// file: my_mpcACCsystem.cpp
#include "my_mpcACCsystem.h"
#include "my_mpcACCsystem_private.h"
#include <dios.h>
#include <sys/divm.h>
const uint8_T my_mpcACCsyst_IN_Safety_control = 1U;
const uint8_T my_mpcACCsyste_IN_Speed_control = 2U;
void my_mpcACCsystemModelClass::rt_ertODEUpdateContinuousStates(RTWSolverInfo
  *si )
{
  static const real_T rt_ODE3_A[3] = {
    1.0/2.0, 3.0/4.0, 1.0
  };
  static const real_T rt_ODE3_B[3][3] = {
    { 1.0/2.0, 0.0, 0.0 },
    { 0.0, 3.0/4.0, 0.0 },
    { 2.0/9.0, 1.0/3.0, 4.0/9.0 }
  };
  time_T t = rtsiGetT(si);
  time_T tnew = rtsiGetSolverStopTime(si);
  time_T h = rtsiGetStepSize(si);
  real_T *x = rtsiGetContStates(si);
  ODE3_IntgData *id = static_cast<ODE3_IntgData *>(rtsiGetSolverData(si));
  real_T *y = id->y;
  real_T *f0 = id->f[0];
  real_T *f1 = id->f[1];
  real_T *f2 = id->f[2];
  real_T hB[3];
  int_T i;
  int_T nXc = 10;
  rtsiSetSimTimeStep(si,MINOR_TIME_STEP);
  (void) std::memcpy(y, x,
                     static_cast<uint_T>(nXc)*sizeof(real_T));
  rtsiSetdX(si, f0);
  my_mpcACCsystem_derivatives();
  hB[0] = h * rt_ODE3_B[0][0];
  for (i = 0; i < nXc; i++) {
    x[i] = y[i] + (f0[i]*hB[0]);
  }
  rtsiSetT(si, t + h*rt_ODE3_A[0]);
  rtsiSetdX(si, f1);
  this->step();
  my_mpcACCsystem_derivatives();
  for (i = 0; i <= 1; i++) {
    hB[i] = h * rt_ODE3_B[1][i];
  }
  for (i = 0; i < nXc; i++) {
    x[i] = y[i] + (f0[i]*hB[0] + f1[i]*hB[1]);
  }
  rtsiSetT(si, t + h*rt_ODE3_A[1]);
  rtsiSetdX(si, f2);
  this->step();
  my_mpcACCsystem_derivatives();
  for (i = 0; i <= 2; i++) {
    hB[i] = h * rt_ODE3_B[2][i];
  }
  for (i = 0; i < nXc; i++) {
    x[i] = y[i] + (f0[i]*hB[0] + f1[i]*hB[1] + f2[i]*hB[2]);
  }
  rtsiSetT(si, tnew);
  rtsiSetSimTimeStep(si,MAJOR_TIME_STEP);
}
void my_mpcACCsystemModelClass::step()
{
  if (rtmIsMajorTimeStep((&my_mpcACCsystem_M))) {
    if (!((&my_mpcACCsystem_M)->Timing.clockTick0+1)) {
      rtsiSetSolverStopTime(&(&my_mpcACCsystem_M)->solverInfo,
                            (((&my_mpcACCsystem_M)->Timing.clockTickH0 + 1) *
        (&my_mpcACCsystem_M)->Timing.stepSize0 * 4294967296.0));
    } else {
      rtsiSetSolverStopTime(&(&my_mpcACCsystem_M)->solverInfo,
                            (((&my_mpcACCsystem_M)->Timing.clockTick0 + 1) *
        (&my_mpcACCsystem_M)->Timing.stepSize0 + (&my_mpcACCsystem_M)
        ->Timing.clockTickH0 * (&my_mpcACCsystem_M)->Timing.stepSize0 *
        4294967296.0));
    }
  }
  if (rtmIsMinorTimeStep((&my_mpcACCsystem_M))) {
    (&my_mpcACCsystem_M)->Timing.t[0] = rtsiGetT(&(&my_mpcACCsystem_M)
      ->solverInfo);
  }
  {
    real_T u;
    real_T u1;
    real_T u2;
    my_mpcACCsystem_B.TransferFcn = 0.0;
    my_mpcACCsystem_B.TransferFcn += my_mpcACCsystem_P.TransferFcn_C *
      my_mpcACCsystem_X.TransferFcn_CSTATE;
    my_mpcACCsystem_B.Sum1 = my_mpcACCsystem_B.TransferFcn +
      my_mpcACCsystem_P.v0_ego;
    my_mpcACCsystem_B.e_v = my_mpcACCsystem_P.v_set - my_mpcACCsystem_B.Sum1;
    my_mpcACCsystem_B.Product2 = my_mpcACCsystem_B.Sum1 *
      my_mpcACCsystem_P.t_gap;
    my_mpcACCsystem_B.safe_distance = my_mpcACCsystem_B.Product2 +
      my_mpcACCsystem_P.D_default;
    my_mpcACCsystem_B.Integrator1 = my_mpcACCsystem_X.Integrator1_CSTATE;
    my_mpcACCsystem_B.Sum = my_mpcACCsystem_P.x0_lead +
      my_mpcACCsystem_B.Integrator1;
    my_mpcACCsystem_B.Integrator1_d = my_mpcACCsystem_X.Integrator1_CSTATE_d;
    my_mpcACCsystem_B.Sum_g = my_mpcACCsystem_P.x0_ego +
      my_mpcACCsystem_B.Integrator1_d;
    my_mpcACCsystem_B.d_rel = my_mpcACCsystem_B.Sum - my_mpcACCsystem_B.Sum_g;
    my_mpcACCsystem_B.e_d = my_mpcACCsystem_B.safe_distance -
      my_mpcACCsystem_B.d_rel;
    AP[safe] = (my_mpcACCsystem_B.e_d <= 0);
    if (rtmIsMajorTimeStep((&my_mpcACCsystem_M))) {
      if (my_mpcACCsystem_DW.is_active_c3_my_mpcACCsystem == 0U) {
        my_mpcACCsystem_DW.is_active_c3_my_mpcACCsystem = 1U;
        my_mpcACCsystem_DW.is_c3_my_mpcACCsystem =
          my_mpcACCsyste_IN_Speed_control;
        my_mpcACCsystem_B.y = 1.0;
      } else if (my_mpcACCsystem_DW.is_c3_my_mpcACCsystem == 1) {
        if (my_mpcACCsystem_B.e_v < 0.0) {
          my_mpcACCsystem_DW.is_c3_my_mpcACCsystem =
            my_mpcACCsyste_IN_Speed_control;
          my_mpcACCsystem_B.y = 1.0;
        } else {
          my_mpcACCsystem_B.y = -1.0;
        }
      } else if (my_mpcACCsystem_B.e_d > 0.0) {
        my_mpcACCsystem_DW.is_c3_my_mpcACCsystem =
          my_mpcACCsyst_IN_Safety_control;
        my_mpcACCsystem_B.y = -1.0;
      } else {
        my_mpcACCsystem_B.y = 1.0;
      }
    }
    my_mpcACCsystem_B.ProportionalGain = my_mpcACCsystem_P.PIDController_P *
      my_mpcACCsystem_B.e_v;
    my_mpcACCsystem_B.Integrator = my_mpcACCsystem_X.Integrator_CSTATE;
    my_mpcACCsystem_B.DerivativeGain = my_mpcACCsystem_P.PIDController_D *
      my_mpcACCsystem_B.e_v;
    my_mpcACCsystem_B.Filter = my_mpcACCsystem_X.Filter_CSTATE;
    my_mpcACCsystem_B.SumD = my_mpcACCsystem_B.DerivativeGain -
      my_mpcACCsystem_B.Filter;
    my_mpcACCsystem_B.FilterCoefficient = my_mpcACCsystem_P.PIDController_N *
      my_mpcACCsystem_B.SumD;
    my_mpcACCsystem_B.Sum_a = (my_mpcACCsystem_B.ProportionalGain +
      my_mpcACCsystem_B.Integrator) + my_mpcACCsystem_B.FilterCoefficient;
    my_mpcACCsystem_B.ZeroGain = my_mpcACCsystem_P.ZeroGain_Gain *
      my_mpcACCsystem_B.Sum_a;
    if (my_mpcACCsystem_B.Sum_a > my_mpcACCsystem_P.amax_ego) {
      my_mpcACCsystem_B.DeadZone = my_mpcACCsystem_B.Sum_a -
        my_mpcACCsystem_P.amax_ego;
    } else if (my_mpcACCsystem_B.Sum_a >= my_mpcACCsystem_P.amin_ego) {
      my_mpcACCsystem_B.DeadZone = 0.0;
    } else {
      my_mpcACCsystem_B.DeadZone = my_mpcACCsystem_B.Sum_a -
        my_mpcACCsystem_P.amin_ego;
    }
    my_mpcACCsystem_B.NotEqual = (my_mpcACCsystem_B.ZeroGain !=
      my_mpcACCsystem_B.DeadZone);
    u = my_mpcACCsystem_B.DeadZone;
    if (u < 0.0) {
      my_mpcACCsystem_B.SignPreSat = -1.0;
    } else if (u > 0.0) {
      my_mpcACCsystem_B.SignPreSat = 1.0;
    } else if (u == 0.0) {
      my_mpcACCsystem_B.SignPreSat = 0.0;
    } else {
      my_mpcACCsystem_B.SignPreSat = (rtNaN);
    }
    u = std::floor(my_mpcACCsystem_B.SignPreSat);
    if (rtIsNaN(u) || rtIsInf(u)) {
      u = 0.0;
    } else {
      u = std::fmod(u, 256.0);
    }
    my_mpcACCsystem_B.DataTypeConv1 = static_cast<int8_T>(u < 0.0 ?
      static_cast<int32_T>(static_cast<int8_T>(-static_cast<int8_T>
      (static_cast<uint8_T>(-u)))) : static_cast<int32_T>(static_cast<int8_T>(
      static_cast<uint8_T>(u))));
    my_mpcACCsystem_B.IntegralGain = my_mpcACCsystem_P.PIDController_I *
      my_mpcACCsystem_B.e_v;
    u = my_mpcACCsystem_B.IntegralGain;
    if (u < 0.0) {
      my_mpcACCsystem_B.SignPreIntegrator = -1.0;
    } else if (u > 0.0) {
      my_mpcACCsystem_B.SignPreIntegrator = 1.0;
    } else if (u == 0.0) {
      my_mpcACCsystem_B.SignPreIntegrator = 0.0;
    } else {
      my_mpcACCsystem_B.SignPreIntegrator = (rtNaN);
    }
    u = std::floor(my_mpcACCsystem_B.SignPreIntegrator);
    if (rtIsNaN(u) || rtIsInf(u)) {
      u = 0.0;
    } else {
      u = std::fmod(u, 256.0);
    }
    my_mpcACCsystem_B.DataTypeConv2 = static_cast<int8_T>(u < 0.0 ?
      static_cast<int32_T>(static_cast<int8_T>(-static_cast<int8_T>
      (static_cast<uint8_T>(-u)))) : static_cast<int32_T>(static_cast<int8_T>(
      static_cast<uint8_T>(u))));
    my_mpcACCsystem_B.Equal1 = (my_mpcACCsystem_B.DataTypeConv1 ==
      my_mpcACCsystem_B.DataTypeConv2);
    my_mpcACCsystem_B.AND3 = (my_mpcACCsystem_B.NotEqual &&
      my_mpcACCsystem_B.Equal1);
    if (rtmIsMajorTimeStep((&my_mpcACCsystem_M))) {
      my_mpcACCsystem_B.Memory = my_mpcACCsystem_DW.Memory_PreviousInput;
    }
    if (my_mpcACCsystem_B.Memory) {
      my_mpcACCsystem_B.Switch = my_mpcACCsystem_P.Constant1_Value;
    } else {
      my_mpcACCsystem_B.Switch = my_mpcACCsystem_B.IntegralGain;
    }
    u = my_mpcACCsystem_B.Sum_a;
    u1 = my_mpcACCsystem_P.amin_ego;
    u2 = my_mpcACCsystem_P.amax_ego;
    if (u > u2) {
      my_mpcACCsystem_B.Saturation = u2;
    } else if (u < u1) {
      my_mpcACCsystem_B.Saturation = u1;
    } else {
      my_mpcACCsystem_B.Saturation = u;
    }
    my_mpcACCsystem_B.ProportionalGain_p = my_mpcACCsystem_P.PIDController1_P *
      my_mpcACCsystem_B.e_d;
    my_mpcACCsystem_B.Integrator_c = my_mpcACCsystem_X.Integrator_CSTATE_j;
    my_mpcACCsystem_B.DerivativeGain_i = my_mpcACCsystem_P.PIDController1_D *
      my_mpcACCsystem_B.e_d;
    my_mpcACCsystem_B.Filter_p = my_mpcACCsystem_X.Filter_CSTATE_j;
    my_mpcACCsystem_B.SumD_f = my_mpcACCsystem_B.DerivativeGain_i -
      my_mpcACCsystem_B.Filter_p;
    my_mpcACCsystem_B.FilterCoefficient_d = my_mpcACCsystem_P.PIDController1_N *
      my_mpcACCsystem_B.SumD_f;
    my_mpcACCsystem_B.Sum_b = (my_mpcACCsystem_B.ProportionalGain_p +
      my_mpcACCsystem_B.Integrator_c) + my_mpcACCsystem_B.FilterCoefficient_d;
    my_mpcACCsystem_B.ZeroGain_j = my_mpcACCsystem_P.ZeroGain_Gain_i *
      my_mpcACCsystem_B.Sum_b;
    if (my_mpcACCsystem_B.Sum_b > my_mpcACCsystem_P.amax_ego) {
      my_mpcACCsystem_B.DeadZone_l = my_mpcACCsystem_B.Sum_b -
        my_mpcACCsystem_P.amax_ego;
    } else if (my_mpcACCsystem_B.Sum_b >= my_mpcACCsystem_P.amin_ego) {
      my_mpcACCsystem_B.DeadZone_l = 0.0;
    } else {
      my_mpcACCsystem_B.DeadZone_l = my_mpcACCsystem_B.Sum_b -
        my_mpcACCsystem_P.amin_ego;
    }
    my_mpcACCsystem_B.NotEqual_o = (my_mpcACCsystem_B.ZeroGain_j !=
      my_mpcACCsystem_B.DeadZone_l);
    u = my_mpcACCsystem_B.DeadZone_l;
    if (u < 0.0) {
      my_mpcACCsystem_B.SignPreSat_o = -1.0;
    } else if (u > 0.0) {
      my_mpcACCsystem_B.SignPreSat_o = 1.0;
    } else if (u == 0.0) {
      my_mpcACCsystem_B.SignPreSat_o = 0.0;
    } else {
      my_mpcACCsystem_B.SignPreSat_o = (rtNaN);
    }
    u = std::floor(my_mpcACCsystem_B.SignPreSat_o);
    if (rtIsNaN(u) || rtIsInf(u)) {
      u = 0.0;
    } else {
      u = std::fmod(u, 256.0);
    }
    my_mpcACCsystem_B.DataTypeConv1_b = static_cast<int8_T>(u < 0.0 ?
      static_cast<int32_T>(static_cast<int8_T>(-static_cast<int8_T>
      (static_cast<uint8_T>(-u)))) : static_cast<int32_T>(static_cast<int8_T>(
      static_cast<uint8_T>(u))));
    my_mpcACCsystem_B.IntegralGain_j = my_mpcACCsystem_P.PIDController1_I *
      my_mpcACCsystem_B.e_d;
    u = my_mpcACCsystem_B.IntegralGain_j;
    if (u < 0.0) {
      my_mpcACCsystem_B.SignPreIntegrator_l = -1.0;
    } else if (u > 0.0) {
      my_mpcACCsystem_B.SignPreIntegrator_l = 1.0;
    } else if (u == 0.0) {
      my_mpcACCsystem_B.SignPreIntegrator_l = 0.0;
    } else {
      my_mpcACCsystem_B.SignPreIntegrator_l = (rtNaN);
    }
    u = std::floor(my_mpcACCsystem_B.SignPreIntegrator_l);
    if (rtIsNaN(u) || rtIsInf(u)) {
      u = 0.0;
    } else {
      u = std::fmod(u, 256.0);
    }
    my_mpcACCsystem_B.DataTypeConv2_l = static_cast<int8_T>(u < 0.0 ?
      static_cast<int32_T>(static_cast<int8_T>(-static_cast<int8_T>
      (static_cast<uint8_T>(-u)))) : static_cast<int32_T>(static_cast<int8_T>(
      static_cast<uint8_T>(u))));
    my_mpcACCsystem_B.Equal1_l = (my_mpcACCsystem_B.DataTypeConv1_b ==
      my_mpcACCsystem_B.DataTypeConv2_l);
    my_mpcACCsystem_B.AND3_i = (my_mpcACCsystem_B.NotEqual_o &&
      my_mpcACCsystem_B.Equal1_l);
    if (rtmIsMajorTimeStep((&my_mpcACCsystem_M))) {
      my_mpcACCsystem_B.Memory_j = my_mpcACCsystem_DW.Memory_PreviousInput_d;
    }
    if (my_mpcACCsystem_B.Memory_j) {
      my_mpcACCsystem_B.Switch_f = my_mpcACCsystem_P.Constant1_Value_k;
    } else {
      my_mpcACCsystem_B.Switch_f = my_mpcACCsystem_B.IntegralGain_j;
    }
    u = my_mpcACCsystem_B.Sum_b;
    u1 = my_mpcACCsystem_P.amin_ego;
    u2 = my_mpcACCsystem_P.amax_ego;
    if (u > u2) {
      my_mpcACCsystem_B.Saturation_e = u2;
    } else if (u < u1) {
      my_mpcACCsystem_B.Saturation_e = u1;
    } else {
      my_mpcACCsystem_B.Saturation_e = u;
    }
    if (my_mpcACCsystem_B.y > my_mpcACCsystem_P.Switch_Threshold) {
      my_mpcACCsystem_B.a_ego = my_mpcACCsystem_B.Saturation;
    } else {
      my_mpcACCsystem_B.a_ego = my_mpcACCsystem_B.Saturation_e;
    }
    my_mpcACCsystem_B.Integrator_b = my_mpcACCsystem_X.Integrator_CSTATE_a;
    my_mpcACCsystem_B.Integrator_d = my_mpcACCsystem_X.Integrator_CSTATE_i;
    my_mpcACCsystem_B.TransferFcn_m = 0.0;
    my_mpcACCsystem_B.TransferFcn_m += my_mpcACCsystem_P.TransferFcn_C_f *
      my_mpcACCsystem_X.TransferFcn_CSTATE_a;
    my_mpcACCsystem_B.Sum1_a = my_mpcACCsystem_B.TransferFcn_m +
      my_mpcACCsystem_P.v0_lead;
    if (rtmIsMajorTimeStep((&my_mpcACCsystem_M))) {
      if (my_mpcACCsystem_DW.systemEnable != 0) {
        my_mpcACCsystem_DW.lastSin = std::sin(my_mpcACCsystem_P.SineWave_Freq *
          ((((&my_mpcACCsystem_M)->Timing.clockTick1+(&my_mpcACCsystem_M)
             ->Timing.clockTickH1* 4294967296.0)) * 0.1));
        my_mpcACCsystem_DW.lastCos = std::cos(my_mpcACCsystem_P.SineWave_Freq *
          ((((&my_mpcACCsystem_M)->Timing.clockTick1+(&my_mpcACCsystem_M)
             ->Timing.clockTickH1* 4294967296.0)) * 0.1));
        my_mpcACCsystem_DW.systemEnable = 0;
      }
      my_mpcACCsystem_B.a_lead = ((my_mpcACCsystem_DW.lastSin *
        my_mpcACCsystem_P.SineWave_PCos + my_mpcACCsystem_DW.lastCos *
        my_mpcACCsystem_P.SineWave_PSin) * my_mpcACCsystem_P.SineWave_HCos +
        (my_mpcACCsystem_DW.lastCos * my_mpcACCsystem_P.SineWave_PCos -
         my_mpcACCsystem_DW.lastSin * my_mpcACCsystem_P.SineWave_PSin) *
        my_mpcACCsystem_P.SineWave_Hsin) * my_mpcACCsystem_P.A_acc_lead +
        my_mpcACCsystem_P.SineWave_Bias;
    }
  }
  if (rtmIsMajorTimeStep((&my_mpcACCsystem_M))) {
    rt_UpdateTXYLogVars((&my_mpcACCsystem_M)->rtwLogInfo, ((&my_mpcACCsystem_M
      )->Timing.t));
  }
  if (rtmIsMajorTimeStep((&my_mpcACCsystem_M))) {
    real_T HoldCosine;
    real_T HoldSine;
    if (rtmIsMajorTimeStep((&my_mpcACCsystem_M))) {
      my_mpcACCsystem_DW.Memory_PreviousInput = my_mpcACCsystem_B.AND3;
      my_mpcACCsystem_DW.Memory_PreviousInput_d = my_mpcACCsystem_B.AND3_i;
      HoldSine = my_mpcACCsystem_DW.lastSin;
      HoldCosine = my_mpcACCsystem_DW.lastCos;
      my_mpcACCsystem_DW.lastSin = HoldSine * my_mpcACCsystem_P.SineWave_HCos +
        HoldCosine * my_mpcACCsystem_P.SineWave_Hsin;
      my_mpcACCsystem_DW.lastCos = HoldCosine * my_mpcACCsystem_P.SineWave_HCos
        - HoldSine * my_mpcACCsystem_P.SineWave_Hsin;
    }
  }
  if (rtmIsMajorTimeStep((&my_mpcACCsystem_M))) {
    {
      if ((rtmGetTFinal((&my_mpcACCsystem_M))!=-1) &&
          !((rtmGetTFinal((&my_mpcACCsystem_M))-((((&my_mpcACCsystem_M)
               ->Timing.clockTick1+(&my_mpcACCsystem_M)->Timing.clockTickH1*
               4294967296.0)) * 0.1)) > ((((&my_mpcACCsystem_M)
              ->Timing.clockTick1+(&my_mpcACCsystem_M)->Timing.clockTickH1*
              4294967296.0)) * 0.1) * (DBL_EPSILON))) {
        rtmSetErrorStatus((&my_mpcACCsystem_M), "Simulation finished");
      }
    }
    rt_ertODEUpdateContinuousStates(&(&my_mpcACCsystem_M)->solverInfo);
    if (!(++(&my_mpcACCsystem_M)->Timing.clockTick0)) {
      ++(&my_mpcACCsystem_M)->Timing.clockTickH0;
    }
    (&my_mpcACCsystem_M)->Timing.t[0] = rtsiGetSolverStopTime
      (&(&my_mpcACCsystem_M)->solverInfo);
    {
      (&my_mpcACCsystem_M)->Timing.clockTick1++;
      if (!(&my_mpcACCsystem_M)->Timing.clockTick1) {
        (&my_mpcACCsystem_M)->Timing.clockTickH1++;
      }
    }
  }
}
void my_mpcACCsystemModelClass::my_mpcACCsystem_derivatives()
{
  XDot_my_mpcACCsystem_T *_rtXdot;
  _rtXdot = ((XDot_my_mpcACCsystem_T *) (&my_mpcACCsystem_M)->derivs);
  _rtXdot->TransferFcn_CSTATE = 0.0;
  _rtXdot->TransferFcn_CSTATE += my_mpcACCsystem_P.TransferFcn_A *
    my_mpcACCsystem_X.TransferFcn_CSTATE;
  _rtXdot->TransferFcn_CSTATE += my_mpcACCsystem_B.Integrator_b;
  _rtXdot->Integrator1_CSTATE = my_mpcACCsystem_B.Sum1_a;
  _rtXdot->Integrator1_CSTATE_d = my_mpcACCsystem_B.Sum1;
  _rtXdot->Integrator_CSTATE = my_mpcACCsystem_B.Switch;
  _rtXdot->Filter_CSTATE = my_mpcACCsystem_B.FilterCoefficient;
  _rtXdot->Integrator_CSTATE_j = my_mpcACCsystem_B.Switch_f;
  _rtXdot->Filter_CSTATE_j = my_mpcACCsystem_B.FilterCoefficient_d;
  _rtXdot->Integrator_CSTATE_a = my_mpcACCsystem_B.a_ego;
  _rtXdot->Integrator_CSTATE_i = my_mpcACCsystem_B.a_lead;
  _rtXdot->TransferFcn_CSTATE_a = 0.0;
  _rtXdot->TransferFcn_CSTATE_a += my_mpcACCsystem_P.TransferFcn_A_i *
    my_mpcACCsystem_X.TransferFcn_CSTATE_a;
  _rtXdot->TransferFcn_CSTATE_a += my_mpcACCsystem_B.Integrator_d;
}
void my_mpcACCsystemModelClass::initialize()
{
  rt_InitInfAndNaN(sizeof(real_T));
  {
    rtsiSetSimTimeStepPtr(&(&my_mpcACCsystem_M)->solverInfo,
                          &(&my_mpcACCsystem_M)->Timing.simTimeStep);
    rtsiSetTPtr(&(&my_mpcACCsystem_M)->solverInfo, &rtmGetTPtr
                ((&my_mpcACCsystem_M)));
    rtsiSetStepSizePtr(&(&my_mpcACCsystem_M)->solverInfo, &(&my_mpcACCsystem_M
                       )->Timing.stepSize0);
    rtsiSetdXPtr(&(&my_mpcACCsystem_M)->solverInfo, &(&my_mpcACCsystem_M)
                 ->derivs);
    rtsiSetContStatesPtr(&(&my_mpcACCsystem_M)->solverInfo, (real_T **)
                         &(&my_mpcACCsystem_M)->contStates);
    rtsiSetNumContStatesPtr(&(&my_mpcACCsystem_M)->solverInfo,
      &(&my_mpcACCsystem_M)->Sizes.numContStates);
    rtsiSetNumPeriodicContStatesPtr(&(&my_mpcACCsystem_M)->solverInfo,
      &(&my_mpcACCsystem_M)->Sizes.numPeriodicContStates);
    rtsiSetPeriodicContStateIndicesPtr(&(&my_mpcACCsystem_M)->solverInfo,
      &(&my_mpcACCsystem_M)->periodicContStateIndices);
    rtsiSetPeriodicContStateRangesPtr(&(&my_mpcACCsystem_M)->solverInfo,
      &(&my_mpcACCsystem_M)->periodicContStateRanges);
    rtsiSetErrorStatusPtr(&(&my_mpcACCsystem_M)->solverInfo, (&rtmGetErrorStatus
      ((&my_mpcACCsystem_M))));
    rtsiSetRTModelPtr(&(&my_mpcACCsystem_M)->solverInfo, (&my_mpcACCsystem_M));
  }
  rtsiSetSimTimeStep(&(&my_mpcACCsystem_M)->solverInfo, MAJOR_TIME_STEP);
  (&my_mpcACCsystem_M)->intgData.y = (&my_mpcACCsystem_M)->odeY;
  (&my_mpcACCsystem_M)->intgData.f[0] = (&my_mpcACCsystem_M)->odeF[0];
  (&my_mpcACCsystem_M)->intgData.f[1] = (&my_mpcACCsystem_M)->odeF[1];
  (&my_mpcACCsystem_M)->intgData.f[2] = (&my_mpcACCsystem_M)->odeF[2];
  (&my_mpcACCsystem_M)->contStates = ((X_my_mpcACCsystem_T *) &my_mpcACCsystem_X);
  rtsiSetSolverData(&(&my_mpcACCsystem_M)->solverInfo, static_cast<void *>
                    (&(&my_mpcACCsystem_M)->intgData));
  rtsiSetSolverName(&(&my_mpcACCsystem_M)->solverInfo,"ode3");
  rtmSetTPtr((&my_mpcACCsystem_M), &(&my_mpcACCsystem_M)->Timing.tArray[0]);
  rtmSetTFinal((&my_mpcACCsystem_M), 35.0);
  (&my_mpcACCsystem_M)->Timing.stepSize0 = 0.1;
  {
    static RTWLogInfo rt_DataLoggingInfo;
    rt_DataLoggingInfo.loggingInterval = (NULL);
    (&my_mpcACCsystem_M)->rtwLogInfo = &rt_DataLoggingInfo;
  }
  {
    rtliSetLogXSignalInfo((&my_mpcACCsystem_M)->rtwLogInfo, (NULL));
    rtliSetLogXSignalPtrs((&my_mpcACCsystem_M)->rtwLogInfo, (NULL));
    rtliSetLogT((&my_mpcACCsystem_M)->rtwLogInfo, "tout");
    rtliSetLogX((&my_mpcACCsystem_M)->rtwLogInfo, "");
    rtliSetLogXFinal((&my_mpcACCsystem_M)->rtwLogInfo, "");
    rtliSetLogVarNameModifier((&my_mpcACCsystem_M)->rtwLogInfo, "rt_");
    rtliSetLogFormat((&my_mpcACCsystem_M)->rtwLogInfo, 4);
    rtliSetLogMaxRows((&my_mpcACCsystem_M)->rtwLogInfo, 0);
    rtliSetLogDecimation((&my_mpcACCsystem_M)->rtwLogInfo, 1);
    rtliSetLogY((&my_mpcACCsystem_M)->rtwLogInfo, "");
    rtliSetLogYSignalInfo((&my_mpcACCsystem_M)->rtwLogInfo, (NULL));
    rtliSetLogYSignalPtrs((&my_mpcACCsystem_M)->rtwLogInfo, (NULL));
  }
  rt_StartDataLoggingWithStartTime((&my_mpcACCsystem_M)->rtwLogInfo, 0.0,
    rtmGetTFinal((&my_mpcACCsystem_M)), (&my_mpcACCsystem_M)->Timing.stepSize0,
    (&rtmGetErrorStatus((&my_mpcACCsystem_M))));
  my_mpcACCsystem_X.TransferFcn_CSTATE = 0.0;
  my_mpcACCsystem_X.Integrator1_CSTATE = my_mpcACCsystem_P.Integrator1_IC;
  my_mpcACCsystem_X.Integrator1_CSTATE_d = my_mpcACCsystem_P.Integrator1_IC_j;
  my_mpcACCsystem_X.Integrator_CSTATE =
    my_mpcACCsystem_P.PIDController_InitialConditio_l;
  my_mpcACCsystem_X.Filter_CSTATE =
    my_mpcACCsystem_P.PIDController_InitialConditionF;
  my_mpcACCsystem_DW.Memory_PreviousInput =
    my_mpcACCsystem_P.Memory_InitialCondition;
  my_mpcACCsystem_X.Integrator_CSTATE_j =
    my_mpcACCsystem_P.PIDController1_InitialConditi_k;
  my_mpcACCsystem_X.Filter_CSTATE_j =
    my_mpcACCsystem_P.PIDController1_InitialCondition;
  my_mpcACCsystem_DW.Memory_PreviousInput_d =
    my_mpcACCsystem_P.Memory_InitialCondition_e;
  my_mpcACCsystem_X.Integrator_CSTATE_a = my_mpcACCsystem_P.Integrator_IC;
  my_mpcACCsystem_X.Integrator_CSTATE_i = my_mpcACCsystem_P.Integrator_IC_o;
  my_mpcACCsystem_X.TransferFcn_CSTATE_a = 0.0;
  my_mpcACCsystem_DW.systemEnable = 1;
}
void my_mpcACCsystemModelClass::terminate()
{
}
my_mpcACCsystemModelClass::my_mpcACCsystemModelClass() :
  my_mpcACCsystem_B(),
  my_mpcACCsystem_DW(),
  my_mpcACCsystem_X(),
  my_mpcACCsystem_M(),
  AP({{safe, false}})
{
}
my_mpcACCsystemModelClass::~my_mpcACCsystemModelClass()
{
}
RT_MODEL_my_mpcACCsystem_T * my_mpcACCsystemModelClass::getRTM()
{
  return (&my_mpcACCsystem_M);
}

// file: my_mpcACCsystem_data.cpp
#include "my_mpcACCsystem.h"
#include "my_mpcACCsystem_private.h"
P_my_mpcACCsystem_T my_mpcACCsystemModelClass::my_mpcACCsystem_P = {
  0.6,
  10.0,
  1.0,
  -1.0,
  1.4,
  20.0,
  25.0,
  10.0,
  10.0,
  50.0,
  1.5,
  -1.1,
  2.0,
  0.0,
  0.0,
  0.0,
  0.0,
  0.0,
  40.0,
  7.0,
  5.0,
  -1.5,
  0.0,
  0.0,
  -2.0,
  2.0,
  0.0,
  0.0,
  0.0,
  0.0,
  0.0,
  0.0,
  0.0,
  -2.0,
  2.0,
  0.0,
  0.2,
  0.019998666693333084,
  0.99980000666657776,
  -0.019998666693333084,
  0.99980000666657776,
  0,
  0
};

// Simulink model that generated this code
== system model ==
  Stateflowchart#1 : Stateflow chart  <- 1: Sum#1, 2: Sum#2
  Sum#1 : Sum  Inputs=+-  <- 1: Constant#1, 2: Sum1
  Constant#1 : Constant  Value=v_set
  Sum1 : Sum  <- 1: TransferFcn, 2: Constant#2
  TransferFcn : TransferFcn  Denominator=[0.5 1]  <- 1: Integrator
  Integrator : Integrator  <- 1: Switch
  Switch : Switch  Criteria=u2 > Threshold  <- 1: PIDController, 2: Stateflowchart#1, 3: PIDController1
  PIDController : pid_lib/PID Controller  Controller=PID  Form=Parallel  TimeDomain=Continuous-time  IntegratorMethod=Forward Euler  P=5  I=2  D=1.5  N=40  InitialConditionForIntegrator=0  ExternalReset=none  LimitOutput=on  UpperSaturationLimit=amax_ego  LowerSaturationLimit=amin_ego  <- 1: Sum#1
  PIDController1 : pid_lib/PID Controller  Controller=PID  Form=Parallel  TimeDomain=Continuous-time  IntegratorMethod=Forward Euler  P=-1.5  I=0  D=-1.1  N=7  InitialConditionForIntegrator=0  ExternalReset=none  LimitOutput=on  UpperSaturationLimit=amax_ego  LowerSaturationLimit=amin_ego  <- 1: Sum#2
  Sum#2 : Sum  Inputs=+-  <- 1: Sum#3, 2: Sum
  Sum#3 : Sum  <- 1: Product2, 2: Constant#3
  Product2 : Product  <- 1: Sum1, 2: Constant#4
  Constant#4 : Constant  Value=t_gap
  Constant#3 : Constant  Value=D_default
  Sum : Sum  Inputs=+-  <- 1: Sum#4, 2: Sum#5
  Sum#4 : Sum  <- 1: Constant#5, 2: Integrator1
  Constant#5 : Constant  Value=x0_lead
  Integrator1 : Integrator  <- 1: Sum#6
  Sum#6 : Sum  <- 1: TransferFcn#1, 2: Constant#6
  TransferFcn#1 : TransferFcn  Denominator=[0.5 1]  <- 1: Integrator#1
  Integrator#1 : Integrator  <- 1: SineWave
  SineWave : Sin  Amplitude=A_acc_lead  Frequency=0.2
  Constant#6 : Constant  Value=v0_lead
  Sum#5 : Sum  <- 1: Constant#7, 2: Integrator#2
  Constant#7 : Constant  Value=x0_ego
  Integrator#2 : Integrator  <- 1: Sum1
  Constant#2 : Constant  Value=v0_ego
== stateflow chart Stateflowchart#1 ==
  state Speed_control
    y=1;
  state Safety_control
    y=-1;
  Speed_control -> Safety_control : [(e_d > 0)]
  (default) -> Speed_control
  Safety_control -> Speed_control : [(e_v<0)]
  data: e_v input; e_d input; y output
